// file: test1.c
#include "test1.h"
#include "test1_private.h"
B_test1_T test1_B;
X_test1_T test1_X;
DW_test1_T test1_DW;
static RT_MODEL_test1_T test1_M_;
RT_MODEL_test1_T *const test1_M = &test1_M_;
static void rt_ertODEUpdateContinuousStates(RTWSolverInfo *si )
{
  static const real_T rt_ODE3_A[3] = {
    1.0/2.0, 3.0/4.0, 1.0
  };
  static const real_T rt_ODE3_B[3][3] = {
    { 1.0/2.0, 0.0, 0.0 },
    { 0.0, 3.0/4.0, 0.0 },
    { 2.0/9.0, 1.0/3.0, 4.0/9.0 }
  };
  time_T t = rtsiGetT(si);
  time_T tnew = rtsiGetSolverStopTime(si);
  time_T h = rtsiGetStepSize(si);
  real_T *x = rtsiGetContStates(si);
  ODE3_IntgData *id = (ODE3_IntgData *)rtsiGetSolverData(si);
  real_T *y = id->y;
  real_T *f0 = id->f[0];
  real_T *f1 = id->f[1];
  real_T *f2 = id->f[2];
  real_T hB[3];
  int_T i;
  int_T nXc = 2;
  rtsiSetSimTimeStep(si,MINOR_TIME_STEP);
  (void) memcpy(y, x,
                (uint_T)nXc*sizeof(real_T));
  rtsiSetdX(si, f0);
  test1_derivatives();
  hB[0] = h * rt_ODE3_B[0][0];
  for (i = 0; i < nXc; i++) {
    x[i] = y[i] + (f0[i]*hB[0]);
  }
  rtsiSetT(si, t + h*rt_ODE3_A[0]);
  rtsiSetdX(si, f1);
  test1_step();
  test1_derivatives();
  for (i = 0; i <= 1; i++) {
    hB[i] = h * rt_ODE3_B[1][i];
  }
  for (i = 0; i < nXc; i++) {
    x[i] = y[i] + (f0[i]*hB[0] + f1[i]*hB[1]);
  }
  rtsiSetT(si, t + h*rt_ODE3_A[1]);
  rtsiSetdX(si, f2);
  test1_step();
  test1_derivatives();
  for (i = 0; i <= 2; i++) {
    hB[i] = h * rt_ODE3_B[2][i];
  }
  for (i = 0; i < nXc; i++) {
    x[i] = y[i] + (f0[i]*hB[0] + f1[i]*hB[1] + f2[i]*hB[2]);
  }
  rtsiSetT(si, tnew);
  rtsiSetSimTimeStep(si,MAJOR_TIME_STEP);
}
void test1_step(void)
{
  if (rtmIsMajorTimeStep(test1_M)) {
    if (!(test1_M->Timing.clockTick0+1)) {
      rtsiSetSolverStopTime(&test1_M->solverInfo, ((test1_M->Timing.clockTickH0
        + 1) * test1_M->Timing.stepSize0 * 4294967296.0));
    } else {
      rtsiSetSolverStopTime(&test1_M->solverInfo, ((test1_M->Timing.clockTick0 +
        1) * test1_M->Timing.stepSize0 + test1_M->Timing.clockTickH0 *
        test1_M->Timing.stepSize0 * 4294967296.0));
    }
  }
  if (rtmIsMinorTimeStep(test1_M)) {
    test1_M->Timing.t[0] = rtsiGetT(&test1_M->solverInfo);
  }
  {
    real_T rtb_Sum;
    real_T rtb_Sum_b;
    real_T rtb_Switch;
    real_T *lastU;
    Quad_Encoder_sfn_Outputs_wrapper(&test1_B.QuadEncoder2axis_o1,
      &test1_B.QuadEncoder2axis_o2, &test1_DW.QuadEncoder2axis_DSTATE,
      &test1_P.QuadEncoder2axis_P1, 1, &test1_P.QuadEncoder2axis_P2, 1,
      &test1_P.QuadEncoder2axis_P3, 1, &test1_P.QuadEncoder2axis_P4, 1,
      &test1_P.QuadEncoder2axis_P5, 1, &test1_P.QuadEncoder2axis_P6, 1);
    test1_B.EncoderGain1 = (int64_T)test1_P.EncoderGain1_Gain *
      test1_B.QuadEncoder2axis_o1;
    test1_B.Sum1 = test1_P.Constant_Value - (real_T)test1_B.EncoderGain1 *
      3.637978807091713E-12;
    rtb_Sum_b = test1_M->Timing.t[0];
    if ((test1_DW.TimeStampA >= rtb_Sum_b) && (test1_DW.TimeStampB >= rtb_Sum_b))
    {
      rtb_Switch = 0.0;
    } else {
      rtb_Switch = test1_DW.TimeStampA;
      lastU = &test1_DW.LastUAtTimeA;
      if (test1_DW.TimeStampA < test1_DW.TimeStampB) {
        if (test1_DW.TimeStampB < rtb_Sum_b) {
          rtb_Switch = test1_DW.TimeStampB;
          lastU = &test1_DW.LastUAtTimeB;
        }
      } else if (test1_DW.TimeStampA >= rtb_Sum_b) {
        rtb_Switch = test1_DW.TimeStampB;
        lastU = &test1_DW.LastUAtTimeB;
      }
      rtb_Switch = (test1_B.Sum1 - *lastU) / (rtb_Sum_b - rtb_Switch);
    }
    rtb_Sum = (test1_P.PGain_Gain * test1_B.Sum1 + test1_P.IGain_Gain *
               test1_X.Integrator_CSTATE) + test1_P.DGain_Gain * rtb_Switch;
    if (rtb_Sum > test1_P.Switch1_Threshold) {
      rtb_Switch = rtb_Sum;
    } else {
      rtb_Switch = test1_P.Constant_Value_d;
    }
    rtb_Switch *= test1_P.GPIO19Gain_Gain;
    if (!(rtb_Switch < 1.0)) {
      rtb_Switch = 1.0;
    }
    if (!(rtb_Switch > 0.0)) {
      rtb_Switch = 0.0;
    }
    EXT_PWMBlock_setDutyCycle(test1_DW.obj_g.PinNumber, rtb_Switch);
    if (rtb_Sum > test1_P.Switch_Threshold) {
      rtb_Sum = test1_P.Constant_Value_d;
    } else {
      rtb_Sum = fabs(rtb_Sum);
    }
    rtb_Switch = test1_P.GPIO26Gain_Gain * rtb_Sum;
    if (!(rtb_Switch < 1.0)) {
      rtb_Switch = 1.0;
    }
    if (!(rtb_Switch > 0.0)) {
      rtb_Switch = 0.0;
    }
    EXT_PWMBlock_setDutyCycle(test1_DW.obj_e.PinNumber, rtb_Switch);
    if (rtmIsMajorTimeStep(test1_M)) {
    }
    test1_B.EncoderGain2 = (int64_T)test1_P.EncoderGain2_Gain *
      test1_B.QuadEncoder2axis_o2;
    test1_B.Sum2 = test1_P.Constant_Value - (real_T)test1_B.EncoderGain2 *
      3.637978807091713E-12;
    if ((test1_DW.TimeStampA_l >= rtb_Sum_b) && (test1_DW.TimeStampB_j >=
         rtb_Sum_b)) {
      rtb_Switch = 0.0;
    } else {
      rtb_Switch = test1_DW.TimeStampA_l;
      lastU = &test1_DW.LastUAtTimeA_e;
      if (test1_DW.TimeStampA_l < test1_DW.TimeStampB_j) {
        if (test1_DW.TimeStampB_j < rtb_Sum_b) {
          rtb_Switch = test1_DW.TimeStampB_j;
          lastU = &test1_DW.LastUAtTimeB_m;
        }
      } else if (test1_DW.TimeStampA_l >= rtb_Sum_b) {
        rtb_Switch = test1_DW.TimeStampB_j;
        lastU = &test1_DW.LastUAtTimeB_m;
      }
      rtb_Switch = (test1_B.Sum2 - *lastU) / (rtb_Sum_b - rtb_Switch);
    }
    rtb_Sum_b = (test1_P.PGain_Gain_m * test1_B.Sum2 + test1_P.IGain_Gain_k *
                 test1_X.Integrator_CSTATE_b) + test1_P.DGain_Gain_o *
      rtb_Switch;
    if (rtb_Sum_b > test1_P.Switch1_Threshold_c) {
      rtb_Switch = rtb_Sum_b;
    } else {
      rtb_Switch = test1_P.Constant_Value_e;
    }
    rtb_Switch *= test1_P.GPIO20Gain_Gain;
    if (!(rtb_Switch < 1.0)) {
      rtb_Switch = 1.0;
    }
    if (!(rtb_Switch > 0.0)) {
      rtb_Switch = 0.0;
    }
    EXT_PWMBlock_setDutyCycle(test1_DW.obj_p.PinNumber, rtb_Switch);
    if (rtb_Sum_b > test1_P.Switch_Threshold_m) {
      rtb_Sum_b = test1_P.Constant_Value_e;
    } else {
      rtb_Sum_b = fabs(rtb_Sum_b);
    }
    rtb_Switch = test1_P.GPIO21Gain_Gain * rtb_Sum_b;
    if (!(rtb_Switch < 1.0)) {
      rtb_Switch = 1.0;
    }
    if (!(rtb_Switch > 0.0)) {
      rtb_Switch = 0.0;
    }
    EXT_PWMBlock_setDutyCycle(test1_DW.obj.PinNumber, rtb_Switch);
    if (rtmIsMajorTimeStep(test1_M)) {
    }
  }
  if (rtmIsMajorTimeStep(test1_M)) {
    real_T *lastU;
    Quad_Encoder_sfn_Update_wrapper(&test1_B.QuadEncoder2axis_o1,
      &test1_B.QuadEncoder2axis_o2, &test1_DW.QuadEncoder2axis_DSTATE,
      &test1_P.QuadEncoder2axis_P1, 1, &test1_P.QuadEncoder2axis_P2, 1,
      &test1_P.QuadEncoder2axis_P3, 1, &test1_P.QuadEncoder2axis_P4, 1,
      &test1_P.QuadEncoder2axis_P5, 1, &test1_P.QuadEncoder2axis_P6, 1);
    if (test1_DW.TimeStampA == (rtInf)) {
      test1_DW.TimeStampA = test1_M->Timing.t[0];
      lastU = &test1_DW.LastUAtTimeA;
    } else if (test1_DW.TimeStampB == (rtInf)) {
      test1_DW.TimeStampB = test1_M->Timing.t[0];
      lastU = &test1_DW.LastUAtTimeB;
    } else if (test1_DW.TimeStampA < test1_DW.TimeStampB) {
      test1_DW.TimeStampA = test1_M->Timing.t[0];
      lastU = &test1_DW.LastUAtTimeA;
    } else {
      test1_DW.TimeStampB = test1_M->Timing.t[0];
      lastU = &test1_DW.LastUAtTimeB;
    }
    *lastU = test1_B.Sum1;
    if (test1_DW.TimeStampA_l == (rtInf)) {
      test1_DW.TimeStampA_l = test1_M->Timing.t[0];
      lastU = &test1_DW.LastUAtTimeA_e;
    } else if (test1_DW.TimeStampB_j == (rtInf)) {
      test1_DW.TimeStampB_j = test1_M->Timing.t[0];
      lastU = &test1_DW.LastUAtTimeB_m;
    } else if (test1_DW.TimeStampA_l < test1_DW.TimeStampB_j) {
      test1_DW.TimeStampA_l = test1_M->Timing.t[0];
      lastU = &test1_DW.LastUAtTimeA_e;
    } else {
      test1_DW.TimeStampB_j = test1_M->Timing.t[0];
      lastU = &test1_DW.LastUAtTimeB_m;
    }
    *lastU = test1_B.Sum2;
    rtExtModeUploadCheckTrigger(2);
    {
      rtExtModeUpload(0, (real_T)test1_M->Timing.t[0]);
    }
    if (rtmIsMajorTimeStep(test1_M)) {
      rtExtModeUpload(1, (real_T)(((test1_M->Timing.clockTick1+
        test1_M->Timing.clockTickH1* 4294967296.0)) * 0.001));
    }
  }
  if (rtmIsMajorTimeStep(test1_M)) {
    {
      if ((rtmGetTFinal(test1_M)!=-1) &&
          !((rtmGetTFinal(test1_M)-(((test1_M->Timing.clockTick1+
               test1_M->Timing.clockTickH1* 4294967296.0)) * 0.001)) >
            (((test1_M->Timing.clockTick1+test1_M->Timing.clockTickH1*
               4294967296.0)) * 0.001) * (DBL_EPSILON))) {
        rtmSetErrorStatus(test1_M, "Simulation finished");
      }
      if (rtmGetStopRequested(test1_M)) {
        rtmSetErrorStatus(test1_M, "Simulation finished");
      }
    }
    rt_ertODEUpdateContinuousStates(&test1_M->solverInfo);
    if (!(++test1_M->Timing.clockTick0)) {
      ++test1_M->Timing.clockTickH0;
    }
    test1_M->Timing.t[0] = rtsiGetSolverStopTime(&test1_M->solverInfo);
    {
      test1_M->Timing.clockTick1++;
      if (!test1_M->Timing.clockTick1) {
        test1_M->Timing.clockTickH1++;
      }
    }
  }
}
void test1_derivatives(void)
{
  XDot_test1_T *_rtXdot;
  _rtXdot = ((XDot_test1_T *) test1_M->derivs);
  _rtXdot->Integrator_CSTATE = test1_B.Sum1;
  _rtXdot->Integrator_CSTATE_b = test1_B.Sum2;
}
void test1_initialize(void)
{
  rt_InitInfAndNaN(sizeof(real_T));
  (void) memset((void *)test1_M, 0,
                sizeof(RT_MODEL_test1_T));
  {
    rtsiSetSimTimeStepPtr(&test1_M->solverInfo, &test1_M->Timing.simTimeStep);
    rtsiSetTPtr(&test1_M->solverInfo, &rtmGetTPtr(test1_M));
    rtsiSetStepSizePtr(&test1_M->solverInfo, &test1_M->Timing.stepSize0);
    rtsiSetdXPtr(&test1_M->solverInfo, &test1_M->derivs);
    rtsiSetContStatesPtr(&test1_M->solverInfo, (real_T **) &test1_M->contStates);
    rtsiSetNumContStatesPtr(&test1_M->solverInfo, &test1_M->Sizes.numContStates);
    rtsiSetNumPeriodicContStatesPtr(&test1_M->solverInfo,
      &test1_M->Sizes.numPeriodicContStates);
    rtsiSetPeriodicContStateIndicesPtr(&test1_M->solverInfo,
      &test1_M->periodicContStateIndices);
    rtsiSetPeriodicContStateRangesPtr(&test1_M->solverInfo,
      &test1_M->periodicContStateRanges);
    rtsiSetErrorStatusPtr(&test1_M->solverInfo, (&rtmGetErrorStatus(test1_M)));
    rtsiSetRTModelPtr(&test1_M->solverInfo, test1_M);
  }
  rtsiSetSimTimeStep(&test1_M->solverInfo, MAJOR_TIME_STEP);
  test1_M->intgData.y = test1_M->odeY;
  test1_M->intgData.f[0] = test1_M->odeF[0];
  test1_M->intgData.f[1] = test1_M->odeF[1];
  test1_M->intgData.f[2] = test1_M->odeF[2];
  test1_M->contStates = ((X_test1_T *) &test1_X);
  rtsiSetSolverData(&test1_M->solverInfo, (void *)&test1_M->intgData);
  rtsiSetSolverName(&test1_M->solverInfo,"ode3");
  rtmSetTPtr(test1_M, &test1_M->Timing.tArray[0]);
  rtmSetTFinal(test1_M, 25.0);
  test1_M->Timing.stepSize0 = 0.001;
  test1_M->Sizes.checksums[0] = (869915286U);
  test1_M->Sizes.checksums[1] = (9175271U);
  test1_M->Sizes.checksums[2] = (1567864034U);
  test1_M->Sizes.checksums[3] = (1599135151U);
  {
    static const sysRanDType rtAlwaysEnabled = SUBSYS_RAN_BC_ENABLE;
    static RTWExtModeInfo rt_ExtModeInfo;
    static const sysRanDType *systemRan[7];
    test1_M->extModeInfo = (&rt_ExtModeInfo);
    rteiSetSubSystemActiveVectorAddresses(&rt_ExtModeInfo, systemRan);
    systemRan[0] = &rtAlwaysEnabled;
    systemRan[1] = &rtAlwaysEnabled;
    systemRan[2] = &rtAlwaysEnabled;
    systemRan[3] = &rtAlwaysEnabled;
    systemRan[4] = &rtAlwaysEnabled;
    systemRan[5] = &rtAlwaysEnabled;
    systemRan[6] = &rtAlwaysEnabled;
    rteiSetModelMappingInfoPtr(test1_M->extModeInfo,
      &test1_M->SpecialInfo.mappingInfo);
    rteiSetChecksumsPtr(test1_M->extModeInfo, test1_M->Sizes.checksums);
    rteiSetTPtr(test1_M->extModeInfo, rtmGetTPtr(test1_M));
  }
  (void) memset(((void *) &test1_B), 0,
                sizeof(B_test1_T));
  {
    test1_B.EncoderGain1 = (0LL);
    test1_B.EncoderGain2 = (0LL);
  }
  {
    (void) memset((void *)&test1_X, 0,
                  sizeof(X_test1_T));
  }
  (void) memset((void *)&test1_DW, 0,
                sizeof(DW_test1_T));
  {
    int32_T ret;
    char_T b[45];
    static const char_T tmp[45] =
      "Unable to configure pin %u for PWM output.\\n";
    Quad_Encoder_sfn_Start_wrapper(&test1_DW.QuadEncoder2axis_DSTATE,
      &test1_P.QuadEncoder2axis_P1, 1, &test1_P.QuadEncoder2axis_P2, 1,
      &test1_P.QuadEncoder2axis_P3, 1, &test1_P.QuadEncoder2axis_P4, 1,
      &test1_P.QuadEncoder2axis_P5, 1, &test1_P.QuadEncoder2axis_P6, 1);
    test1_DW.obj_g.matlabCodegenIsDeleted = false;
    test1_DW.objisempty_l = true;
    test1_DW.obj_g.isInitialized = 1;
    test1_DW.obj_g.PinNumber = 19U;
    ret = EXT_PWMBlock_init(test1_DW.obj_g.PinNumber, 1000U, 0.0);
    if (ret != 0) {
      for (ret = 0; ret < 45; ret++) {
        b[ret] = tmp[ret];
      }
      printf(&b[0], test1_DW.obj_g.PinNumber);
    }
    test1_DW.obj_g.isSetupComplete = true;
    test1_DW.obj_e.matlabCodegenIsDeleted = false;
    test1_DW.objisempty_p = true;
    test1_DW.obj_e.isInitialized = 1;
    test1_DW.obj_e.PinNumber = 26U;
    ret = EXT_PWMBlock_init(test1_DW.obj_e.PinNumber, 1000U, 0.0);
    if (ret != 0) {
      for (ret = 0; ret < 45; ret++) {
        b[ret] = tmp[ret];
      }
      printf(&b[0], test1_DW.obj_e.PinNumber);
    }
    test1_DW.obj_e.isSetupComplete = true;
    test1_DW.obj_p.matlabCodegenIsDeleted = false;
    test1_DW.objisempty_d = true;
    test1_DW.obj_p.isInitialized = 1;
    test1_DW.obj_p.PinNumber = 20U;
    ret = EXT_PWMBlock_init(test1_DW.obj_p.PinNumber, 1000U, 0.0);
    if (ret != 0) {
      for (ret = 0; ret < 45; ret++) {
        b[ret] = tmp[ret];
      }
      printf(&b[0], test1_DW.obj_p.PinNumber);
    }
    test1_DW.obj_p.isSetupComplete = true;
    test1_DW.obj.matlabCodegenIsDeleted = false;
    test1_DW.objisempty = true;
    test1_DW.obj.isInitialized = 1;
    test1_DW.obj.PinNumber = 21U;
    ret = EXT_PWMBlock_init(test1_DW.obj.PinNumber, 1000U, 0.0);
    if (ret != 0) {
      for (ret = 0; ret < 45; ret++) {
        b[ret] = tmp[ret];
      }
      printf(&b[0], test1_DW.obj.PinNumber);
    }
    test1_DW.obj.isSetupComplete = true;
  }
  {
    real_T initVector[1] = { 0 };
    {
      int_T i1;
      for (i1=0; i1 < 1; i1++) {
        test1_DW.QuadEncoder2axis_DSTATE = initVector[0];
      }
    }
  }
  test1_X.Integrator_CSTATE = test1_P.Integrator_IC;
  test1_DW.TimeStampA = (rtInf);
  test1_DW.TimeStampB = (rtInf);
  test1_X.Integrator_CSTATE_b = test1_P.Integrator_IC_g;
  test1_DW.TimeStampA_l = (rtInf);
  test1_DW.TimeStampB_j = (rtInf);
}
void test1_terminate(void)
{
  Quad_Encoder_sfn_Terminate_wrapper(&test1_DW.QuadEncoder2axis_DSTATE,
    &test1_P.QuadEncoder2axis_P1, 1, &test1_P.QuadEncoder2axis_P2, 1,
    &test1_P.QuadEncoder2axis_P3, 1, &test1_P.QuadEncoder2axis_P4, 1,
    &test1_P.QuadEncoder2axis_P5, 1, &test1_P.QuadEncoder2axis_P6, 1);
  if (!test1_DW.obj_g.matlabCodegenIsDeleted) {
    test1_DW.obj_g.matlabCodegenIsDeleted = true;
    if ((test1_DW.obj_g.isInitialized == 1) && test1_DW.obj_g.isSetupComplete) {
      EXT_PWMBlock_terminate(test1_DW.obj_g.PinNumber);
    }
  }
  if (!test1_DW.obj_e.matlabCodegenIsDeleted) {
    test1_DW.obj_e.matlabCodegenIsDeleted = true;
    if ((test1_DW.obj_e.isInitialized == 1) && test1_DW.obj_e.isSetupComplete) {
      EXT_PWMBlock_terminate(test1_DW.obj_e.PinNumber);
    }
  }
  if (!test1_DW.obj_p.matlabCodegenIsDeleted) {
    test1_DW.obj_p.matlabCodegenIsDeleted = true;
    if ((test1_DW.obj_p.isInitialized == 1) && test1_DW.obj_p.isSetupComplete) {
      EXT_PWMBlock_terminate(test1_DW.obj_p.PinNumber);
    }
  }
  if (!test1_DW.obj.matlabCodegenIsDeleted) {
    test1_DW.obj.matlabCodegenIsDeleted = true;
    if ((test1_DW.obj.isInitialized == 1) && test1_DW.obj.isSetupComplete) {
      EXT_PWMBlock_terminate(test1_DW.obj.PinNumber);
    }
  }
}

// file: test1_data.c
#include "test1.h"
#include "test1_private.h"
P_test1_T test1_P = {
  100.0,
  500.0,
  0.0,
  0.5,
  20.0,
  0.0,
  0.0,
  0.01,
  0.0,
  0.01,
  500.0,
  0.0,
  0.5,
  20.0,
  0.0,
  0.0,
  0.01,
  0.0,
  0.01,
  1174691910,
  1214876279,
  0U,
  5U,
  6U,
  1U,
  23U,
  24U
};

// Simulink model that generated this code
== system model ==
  PWM : raspberrypiBasiclib/PWM  Frequency=1000  <- 1: GPIO19Gain
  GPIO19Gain : Gain  Gain=1/100  <- 1: Switch1
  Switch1 : Switch  Criteria=u2 > Threshold  <- 1: Sum, 2: Sum, 3: Constant
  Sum : Sum  Inputs=+++  <- 1: PGain, 2: IGain, 3: DGain
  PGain : Gain  Gain=500  <- 1: Sum1
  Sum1 : Sum  Inputs=+-  <- 1: Constant#1, 2: EncoderGain1
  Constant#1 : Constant  Value=100
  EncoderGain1 : Gain  Gain=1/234  <- 1: QuadEncoder2axis
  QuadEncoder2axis : S-Function  FunctionName=Quad_Encoder_sfn
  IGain : Gain  Gain=0.5  <- 1: Integrator
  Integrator : Integrator  <- 1: Sum1
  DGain : Gain  Gain=20  <- 1: Derivative#1
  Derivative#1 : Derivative  <- 1: Sum1
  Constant : Constant  Value=0
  PWM#1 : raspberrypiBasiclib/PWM  Frequency=1000  <- 1: GPIO26Gain
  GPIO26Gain : Gain  Gain=1/100  <- 1: Switch
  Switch : Switch  Criteria=u2 > Threshold  <- 1: Constant, 2: Sum, 3: Abs#1
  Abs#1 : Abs  <- 1: Sum
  PWM#2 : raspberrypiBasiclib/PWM  Frequency=1000  <- 1: GPIO20Gain
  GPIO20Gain : Gain  Gain=1/100  <- 1: Switch#1
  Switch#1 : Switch  Criteria=u2 > Threshold  <- 1: Sum#1, 2: Sum#1, 3: Constant#2
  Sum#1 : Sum  Inputs=+++  <- 1: Gain#1, 2: Gain#2, 3: Gain#3
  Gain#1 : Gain  Gain=500  <- 1: Sum2
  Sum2 : Sum  Inputs=-+  <- 1: EncoderGain2, 2: Constant#1
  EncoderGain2 : Gain  Gain=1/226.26  <- 1: QuadEncoder2axis/2
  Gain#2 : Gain  Gain=0.5  <- 1: Integrator#1
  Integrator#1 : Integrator  <- 1: Sum2
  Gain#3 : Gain  Gain=20  <- 1: Derivative#2
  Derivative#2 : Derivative  <- 1: Sum2
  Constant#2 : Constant  Value=0
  PWM#3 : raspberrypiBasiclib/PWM  Frequency=1000  <- 1: GPIO21Gain
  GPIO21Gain : Gain  Gain=1/100  <- 1: Switch#2
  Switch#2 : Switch  Criteria=u2 > Threshold  <- 1: Constant#2, 2: Sum#1, 3: Abs#2
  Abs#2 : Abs  <- 1: Sum#1
